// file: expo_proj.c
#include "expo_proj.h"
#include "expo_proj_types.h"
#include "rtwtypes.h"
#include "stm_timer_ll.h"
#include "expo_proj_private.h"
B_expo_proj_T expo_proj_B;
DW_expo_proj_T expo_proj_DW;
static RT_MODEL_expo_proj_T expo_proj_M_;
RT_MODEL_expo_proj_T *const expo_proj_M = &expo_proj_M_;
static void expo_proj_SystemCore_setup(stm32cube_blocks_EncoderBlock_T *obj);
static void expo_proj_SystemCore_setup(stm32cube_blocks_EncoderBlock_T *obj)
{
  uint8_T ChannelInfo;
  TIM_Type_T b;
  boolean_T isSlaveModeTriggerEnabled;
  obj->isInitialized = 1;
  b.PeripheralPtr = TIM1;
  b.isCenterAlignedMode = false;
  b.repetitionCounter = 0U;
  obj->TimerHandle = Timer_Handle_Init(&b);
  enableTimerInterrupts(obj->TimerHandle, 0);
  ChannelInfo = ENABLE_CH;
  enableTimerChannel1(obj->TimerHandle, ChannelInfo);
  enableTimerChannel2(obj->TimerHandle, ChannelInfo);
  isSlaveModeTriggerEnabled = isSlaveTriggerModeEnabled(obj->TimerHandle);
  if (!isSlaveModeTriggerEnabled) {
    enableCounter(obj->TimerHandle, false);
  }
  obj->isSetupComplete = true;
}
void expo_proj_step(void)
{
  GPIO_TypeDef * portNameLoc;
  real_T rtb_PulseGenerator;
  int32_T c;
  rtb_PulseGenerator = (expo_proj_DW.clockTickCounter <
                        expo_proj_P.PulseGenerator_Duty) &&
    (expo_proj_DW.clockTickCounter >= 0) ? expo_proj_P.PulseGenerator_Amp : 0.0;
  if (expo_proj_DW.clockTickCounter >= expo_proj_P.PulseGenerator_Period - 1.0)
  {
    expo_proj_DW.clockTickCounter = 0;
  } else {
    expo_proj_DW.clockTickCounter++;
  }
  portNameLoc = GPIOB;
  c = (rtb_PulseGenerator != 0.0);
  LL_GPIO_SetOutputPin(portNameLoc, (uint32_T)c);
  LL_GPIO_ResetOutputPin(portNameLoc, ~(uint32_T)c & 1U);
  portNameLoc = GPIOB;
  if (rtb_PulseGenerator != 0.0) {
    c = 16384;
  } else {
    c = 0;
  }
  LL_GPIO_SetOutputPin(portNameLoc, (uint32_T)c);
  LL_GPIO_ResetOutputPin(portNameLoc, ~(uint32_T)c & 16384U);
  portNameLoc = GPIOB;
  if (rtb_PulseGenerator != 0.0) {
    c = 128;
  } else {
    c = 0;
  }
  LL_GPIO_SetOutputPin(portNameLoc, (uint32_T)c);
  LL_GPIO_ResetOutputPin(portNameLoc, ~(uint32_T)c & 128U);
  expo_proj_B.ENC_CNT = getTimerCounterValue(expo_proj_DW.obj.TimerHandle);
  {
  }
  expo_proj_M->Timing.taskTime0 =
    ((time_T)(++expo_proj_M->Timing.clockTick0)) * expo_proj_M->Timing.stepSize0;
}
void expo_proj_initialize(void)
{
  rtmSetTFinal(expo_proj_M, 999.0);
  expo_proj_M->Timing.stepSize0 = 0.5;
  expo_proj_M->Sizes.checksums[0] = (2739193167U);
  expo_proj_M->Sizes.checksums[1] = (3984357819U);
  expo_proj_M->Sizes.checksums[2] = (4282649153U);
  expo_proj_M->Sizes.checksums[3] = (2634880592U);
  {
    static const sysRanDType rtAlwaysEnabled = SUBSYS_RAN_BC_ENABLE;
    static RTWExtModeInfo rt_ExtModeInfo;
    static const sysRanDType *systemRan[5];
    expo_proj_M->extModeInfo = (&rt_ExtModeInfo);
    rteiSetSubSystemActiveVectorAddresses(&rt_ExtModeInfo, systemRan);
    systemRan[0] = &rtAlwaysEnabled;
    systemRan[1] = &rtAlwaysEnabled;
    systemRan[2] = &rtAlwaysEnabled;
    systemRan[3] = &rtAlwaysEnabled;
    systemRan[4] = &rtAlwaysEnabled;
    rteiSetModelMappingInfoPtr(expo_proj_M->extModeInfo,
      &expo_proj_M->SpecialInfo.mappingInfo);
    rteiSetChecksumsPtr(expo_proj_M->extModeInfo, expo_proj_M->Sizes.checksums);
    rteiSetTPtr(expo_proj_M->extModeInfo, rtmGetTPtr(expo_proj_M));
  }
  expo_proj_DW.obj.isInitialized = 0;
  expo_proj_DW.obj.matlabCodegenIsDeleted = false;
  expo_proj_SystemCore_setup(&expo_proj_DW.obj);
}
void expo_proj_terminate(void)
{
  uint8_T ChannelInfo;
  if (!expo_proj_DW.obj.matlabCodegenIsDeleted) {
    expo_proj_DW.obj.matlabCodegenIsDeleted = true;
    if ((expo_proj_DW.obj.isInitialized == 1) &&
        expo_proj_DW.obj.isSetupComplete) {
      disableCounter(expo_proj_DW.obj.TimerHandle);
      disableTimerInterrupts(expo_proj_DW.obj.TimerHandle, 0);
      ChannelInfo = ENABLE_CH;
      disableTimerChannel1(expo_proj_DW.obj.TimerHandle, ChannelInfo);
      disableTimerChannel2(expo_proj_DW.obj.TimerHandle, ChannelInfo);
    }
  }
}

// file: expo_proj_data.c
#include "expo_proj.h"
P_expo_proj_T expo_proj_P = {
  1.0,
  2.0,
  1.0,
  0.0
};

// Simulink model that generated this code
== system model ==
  Encoder#1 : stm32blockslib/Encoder
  DigitalPortWrite#1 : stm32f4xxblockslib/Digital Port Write  <- 1: PulseGenerator
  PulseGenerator : DiscretePulseGenerator  Period=1  PulseWidth=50
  DigitalPortWrite#2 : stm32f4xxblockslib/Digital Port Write  <- 1: PulseGenerator
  DigitalPortWrite#3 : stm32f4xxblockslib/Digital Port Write  <- 1: PulseGenerator
